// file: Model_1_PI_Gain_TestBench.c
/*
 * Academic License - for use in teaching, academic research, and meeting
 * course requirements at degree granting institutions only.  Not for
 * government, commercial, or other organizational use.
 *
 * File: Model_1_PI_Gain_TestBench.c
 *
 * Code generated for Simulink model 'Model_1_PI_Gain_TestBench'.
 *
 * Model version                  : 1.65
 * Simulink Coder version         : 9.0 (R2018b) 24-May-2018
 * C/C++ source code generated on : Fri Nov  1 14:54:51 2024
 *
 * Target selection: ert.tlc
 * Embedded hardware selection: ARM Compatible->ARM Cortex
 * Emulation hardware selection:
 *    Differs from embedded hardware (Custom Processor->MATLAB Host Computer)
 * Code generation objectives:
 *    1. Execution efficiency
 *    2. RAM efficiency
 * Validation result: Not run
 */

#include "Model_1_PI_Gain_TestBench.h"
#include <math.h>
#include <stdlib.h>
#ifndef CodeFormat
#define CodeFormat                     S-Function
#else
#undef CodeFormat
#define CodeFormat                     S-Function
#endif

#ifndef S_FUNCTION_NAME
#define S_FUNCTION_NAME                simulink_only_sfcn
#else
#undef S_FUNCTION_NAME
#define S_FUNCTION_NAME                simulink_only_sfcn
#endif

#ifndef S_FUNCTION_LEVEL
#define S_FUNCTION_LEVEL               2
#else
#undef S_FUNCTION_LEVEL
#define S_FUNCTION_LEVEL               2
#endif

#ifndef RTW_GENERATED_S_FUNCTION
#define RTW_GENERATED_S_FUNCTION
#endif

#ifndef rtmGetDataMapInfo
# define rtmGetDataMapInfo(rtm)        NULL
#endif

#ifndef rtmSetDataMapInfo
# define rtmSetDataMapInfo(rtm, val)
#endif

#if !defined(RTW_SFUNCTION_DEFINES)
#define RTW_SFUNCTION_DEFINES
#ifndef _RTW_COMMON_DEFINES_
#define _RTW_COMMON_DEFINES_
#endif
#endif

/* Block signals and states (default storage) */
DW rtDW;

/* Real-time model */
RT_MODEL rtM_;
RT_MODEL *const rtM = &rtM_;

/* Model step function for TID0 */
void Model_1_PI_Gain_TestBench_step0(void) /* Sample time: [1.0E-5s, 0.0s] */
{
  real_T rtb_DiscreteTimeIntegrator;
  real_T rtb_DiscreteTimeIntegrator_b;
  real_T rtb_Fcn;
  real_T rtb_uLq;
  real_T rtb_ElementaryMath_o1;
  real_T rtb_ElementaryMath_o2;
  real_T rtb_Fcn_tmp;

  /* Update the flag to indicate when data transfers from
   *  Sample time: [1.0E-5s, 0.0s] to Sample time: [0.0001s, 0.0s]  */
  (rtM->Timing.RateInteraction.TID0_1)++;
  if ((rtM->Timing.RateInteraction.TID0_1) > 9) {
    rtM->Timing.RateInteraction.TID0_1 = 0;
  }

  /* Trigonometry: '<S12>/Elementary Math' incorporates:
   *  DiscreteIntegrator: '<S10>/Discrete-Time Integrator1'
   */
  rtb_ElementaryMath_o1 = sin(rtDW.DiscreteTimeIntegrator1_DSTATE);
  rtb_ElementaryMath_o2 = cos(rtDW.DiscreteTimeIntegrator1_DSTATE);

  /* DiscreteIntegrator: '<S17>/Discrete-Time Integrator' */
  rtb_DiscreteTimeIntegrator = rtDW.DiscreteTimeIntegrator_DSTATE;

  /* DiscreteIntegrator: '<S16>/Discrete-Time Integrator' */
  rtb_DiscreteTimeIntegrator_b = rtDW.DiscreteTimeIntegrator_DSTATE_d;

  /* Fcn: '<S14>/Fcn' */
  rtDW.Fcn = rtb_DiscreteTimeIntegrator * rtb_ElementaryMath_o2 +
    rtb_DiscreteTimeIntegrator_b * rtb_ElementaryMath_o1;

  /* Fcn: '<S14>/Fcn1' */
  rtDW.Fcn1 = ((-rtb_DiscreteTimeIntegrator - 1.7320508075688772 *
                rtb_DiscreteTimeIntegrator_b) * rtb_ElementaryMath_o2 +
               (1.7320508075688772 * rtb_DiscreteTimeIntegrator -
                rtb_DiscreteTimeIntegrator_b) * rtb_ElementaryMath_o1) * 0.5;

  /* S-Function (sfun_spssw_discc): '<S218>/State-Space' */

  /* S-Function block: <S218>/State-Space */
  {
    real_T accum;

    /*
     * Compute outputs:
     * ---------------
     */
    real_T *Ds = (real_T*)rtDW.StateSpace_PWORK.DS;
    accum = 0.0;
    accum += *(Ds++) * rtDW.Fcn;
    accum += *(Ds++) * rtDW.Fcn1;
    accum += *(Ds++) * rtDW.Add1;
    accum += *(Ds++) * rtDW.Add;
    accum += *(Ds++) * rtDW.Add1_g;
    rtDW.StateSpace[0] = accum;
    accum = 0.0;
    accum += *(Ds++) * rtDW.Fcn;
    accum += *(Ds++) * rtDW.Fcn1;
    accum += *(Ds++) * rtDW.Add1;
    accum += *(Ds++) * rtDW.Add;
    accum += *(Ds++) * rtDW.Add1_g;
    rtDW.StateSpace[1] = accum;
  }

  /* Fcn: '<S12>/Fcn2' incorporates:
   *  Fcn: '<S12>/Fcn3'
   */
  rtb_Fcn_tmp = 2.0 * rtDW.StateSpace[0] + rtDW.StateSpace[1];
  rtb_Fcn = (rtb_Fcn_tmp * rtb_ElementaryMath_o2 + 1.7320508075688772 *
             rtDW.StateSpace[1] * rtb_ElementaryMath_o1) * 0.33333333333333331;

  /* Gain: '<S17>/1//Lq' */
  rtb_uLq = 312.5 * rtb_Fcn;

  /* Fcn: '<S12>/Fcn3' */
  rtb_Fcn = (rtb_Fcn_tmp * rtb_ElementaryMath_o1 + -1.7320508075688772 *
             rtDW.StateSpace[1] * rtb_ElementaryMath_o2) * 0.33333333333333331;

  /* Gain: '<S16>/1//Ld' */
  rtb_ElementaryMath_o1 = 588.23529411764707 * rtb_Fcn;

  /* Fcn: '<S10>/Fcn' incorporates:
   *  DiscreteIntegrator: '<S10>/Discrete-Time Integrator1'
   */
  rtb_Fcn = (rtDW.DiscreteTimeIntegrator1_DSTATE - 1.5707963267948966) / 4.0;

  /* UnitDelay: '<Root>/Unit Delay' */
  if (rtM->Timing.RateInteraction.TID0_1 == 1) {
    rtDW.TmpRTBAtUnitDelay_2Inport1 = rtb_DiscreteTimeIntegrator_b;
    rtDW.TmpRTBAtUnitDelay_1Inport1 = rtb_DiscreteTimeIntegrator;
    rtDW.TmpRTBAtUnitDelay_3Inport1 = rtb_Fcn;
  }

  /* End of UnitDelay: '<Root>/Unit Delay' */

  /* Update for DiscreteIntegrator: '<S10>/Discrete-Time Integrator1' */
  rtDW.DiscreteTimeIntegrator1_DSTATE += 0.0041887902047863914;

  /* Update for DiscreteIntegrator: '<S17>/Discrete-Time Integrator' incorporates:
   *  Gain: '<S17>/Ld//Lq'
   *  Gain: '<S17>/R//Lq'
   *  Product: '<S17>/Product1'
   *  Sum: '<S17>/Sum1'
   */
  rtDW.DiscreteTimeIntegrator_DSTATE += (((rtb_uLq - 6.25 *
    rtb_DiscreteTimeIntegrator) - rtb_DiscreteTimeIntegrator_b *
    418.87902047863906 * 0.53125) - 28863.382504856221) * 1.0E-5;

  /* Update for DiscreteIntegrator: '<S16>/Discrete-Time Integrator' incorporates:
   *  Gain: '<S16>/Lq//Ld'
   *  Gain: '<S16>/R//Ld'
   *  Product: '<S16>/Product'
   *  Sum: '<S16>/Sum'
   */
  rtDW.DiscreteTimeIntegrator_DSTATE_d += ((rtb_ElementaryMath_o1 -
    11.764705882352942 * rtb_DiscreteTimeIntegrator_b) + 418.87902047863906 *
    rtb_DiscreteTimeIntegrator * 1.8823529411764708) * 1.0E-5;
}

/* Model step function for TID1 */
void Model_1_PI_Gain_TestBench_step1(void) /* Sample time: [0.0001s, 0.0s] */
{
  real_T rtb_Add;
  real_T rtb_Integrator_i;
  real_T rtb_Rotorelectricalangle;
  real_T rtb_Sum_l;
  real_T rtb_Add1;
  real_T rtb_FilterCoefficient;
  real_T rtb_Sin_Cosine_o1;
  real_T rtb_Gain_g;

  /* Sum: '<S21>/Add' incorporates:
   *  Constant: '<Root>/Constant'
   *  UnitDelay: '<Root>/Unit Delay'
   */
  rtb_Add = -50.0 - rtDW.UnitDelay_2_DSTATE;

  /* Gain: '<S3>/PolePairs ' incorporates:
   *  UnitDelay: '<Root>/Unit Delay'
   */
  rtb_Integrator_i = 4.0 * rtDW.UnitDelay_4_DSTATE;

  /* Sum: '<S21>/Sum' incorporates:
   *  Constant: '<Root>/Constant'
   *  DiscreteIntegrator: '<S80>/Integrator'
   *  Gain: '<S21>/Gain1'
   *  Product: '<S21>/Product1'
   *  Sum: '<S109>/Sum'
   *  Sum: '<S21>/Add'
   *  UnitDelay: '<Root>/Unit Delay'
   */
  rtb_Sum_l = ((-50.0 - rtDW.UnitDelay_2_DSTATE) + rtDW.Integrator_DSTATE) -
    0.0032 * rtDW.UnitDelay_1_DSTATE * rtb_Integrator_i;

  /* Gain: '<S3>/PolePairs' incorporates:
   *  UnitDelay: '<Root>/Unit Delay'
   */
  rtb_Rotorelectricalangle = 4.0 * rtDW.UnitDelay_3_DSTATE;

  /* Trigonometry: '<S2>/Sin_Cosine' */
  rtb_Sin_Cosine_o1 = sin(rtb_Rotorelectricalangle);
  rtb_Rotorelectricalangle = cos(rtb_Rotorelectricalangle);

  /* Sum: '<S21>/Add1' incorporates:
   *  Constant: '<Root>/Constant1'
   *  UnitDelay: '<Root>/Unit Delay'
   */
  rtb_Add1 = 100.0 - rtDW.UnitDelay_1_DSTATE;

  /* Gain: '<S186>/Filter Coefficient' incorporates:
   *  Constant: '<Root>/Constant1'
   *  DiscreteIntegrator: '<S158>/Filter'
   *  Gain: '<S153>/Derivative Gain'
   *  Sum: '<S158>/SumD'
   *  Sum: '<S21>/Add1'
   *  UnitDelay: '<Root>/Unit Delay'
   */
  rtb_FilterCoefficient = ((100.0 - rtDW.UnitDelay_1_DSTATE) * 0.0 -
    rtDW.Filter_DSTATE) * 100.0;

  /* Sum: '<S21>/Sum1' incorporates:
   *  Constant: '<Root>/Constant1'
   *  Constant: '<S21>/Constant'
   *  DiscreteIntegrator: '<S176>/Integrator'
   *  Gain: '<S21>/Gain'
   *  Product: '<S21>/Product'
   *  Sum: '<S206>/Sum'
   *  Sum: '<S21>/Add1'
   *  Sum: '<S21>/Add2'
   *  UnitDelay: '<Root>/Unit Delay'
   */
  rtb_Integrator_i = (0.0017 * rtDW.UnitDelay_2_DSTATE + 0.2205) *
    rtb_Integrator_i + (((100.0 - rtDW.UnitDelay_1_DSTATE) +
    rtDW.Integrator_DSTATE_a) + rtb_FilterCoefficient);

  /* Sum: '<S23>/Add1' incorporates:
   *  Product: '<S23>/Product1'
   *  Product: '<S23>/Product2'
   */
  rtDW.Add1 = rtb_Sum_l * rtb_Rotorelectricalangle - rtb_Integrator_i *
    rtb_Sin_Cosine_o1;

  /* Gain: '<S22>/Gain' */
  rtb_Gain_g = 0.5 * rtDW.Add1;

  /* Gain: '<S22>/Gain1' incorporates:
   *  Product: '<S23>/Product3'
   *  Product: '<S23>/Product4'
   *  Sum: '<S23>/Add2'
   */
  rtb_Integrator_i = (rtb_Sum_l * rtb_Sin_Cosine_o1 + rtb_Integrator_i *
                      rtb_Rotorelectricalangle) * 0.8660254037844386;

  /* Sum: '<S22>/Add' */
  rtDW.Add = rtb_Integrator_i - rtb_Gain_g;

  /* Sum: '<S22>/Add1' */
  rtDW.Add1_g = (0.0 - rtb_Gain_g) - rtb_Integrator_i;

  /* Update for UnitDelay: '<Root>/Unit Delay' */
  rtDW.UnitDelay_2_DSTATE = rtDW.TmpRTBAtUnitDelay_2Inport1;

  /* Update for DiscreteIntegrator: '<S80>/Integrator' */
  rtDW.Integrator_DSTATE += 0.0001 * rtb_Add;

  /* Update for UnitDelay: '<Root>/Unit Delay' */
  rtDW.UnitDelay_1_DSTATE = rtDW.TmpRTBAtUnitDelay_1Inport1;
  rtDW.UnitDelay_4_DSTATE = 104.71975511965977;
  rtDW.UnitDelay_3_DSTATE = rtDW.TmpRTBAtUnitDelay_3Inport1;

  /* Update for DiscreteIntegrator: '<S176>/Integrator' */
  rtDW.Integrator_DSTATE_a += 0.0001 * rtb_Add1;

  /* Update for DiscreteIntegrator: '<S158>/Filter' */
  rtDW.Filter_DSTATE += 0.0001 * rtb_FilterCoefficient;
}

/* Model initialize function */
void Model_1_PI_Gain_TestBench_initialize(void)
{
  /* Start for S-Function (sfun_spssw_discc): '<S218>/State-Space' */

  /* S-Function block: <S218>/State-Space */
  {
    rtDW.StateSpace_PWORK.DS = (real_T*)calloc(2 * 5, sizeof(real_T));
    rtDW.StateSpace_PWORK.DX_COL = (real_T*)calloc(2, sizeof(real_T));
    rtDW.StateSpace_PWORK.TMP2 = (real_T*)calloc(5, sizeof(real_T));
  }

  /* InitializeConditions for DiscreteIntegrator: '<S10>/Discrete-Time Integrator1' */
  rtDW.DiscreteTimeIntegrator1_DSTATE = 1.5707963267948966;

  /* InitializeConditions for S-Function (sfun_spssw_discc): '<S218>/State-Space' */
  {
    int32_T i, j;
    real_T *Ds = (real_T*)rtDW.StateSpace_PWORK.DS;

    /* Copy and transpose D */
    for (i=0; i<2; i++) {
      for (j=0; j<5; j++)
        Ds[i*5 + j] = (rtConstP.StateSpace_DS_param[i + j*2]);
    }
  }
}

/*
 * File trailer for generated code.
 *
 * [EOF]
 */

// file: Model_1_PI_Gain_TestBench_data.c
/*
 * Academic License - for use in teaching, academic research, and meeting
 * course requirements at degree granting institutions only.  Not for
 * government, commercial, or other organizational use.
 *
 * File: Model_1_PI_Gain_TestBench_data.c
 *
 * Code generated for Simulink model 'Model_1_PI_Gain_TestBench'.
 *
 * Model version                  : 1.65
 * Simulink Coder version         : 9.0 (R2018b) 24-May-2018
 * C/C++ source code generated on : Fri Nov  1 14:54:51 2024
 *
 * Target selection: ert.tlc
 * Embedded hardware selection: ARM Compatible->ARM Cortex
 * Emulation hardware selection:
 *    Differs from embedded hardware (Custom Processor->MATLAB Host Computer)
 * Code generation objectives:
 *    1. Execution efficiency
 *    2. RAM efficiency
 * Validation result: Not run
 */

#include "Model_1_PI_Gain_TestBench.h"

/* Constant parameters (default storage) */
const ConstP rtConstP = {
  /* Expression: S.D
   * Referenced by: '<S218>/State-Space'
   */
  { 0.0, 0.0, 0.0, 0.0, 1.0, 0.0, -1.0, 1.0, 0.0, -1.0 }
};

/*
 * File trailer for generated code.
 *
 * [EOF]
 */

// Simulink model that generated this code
simulink model "Model_1_PI_Gain_TestBench"  (R2018b)
settings: Solver=FixedStepDiscrete  StartTime=0.0  StopTime=0.3  MaxStep=1e-4  RelTol=1e-3
values from neighbouring files (symbols this model uses):
  Gain_I = 1    [Model_1_Initialization.m]
  Gain_P = 1    [Model_1_Initialization.m]
  Id_reference = -50    [Model_1_Initialization.m]
  Iq_reference = 100    [Model_1_Initialization.m]
  Lambda_m = 0.2205    [Model_1_Initialization.m]
  Ld = 1.7e-3    (= 0.0017)    [Model_1_Initialization.m]
  Lq = 3.2e-3    (= 0.0032)    [Model_1_Initialization.m]
  Polepairs = 4    [Model_1_Initialization.m]
  Rs = 0.02    [Model_1_Initialization.m]
libraries: powerlib x6, simulink x2

== system Model_1_PI_Gain_TestBench ==
  note: Copyright 2018 The MathWorks, Inc.
  note: - Current closed-loop control
      | - Try Simulink Design Optimization(Analysis -> Response Optimization) to automate tuning the PI controller .  Initial condition: speed = 1000 rpm. (kp, ki) = (1,1)
      | - After tuning the current loop, try the simulation without dynamic decoupling control.
  note: Controller
  note: Plant
  note: FOC Control of PMSM
  " " : Subsystem
  Bus_Selector2 : BusSelector  OutputSignals=Stator current is_q (A)
  Constant : Constant  Value=Id_reference
  Constant1 : Constant  Value=Iq_reference  VectorParams1D=off
  FOC_Current_Control : Subsystem
  Mux : Mux  Inputs=2
  Scope2 : Scope
  Subsystem : Subsystem
  Subsystem1 : Subsystem
  Unit Delay : UnitDelay  SampleTime=1e-4
  powergui : powerlib/powergui  SimulationMode=Continuous  SampleTime=1e-5  frequency=60  Iterations=50  frequencyindice=0  Pbase=100e6  ErrMax=1e-4  UnitsV=kV  UnitsW=MW  buscounter=0  FunctionMessages=off  echomessages=off  EnableUseOfTLC=off  CurrentSourceSwitches=off  DisableSnubberDevices=off  DisableRonSwitches=off  DisableVfSwitches=off  DisplayEquations=off  SolverType=Tustin/Backward Euler (TBE)  Interpol=off  ExternalGateDelay=off  methode=off  Ts=100  x0status=blocks  SPID=on  SwTol=0  HookPort=off  RestoreLinks=warning  ResistiveCurrentMeasurement=off  Frange=[0:2:500]  Ylog=off  Xlog=on  ShowGrid=off  save=off  variable=ZData  structure=0  ZoomFFT=on  StartTime=0.0  cycles=1  DisplayStyle=1  fundamental=60  FreqAxis=off  MaxFrequency=1000  frequencyindicesteady=1  RmsSteady=1  display=off
  Scope : Scope
  Scope1 : Scope
  wires:
  FOC_Current_Control/1(Phase_Voltage) -> Subsystem1/1(In1)
  " "/1(measurements) -> Unit Delay/1, Bus_Selector2/1
  Subsystem/3(Out2) -> FOC_Current_Control/3(iq_feedback)
  Subsystem/4(Out3) -> FOC_Current_Control/4(id_feedback)
  Subsystem1/1(Out1) -> " "/1(Vabc)
  Unit Delay/1 -> Subsystem/3(PMSM_Measurements)
  Subsystem/5(Out1) -> FOC_Current_Control/5(speed_we)
  Subsystem/6(Out4) -> FOC_Current_Control/6(theta)
  Mux/1 -> Scope2/1
  Bus_Selector2/1 -> Mux/2  "<Stator current is_q (A)>"
  Constant/1 -> Subsystem/2(id_ref)
  Constant1/1 -> Mux/1, Subsystem/1(iq_ref)  "Iq_reference"
  Subsystem/1(Out6) -> FOC_Current_Control/1(iq_reference)
  Subsystem/2(Out5) -> FOC_Current_Control/2(id_reference)

== system Model_1_PI_Gain_TestBench/  ==
  Vabc : Inport
  Bus Creator : BusCreator  Inputs=4
  Bus Selector : BusSelector  OutputSignals=Stator current is_a (A),Stator current is_b (A),Stator current is_c (A),Stator current is_q (A),Stator current is_d (A),Rotor angle thetam (rad),Rotor speed wm (rad/s)
  Mux : Mux  Inputs=3
  Permanent Magnet Synchronous Machine [0.002 0.01 3 0] : powerlib/Machines/Permanent Magnet Synchronous Machine  NbPhases=3  FluxDistribution=Sinusoidal  RotorType=Salient-pole  MechanicalLoad=Speed w  PresetModel=No  ShowDetailedParameters=on  MeasurementBus=off  Resistance=Rs  Inductance=8.5e-3  dqInductances=[Ld,Lq]  La=0.000395  MachineConstant=Flux linkage established by magnets (V.s)  Flux=Lambda_m  VoltageCst=159.9771  TorqueCst=1.323  Flat=120  Mechanical=[0.0027 0.001 4 0]  PolePairs=Polepairs  InitialConditions=[0,0, 0,0]  InitialConditions5ph=[0 0 0 0 0 0]  TsPowergui=0  TsBlock=-1  RefAngle=Aligned with phase A axis (original Park)
  Terminator : Terminator
  ideal_voltage_so : Subsystem  VariantControl=variantPwm == enumPwm.behavior
  rpm : Constant  Value=1000
  "rpm -> rad/s" : Gain  Gain=2*pi/60
  measurements : Outport
  wires:
  Vabc/1 -> ideal_voltage_so/1(vabc)
  rpm/1 -> "rpm -> rad/s"/1
  Bus Selector/4 -> Bus Creator/1  "<Stator current is_q (A)>"
  Bus Selector/5 -> Bus Creator/2  "<Stator current is_d (A)>"
  Bus Selector/6 -> Bus Creator/3  "<Rotor angle thetam (rad)>"
  Bus Creator/1 -> measurements/1
  Bus Selector/1 -> Mux/1  "<Stator current is_a (A)>"
  Bus Selector/2 -> Mux/2  "<Stator current is_b (A)>"
  Bus Selector/3 -> Mux/3  "<Stator current is_c (A)>"
  Mux/1 -> Terminator/1
  Permanent Magnet Synchronous Machine [0.002 0.01 3 0]/1 -> Bus Selector/1
  Bus Selector/7 -> Bus Creator/4  "<Rotor speed wm (rad/s)>"
  "rpm -> rad/s"/1 -> Permanent Magnet Synchronous Machine [0.002 0.01 3 0]/1
  connections:
  Permanent Magnet Synchronous Machine [0.002 0.01 3 0]/LConn1 -- ideal_voltage_so/RConn1
  Permanent Magnet Synchronous Machine [0.002 0.01 3 0]/LConn2 -- ideal_voltage_so/RConn2
  Permanent Magnet Synchronous Machine [0.002 0.01 3 0]/LConn3 -- ideal_voltage_so/RConn3

== system Model_1_PI_Gain_TestBench/FOC_Current_Control ==
  iq_reference : Inport  SampleTime=1e-4
  id_reference : Inport  Port=2  SampleTime=1e-4
  iq_feedback : Inport  Port=3  SampleTime=1e-4
  id_feedback : Inport  Port=4  SampleTime=1e-4
  speed_we : Inport  Port=5  SampleTime=1e-4
  theta : Inport  Port=6  SampleTime=1e-4
  Current Controller : Subsystem
  Inverse Clarke Transform : Subsystem
  Inverse Park Transform : Subsystem
  Sin_Cosine : Trigonometry  Operator=sincos
  Phase_Voltage : Outport  SampleTime=1e-4
  wires:
  Inverse Clarke Transform/1(ABC) -> Phase_Voltage/1
  Sin_Cosine/2 -> Inverse Park Transform/4(Cos_Coefficient)
  Sin_Cosine/1 -> Inverse Park Transform/3(Sin_Coefficient)
  theta/1 -> Sin_Cosine/1
  Current Controller/2(vq_reference) -> Inverse Park Transform/2(Q)
  Current Controller/1(vd_reference) -> Inverse Park Transform/1(D)
  Inverse Park Transform/1(Alpha) -> Inverse Clarke Transform/1(Alpha)
  Inverse Park Transform/2(Beta) -> Inverse Clarke Transform/2(Beta)
  id_feedback/1 -> Current Controller/3(id_feedback)
  iq_feedback/1 -> Current Controller/4(iq_feedback)
  speed_we/1 -> Current Controller/5(spd_we)
  iq_reference/1 -> Current Controller/1(iq_reference)
  id_reference/1 -> Current Controller/2(id_reference)

== system Model_1_PI_Gain_TestBench/Subsystem ==
  note: Continuous To Discrete
  iq_ref : Inport
  id_ref : Inport  Port=2
  PMSM_Measurements : Inport  Port=3
  Bus_Selector2 : BusSelector  OutputSignals=Stator current is_q (A),Stator current is_d (A),Rotor speed wm (rad/s),Rotor angle thetam (rad)
  PolePairs : Gain  Gain=Polepairs
  "PolePairs " : Gain  Gain=Polepairs
  Rate_Transition{1..6} (6 alike) : RateTransition  Integrity=off  Deterministic=off
  Out6 : Outport
  Out5 : Outport  Port=2
  Out2 : Outport  Port=3
  Out3 : Outport  Port=4
  Out1 : Outport  Port=5
  Out4 : Outport  Port=6
  wires:
  Rate_Transition4/1 -> Out4/1
  Bus_Selector2/2 -> Rate_Transition3/1  "<Stator current is_d (A)>"
  id_ref/1 -> Rate_Transition5/1
  iq_ref/1 -> Rate_Transition6/1
  Bus_Selector2/1 -> Rate_Transition2/1  "<Stator current is_q (A)>"
  Bus_Selector2/4 -> PolePairs/1  "<Rotor angle thetam (rad)>"
  PMSM_Measurements/1 -> Bus_Selector2/1
  PolePairs/1 -> Rate_Transition4/1  "Rotor electrical angle"
  Rate_Transition5/1 -> Out5/1
  Rate_Transition6/1 -> Out6/1
  Rate_Transition2/1 -> Out2/1
  Rate_Transition3/1 -> Out3/1
  Rate_Transition1/1 -> Out1/1
  Bus_Selector2/3 -> "PolePairs "/1  "<Rotor speed wm (rad/s)>"
  "PolePairs "/1 -> Rate_Transition1/1  "Rotor electrical angular speed"

== system Model_1_PI_Gain_TestBench/Subsystem1 ==
  In1 : Inport
  Rate_Transition1 : RateTransition  Integrity=off
  Out1 : Outport
  wires:
  In1/1 -> Rate_Transition1/1
  Rate_Transition1/1 -> Out1/1

== system Model_1_PI_Gain_TestBench/ /ideal_voltage_so ==
  note: PWM Peripheral And Inverter
  vabc : Inport
  Controlled_Voltage_Source1 : powerlib/Electrical Sources/Controlled Voltage Source  Initialize=off  Source_Type=DC  Amplitude=12  Phase=0  Frequency=0  Measurements=None
  Controlled_Voltage_Source2 : powerlib/Electrical Sources/Controlled Voltage Source  Initialize=off  Source_Type=DC  Amplitude=12  Phase=0  Frequency=0  Measurements=None
  Controlled_Voltage_Source3 : powerlib/Electrical Sources/Controlled Voltage Source  Initialize=off  Source_Type=DC  Amplitude=12  Phase=0  Frequency=0  Measurements=None
  Ground2 : powerlib/Elements/Ground  LConnTagsString=a
  Selector3 : Selector  InputPortWidth=3  IndexOptions=Index vector (dialog)  Indices=[1]  OutputSizes=1
  Selector4 : Selector  InputPortWidth=3  IndexOptions=Index vector (dialog)  Indices=2  OutputSizes=1
  Selector5 : Selector  InputPortWidth=3  IndexOptions=Index vector (dialog)  Indices=3  OutputSizes=1
  A : PMIOPort  Tag=PMCPort  Side=Right
  B : PMIOPort  Tag=PMCPort  Port=2  Side=Right
  C : PMIOPort  Tag=PMCPort  Port=3  Side=Right
  wires:
  vabc/1 -> Selector4/1, Selector5/1, Selector3/1
  Selector5/1 -> Controlled_Voltage_Source3/1
  Selector4/1 -> Controlled_Voltage_Source2/1
  Selector3/1 -> Controlled_Voltage_Source1/1
  connections:
  C/RConn1 -- Controlled_Voltage_Source3/RConn1
  B/RConn1 -- Controlled_Voltage_Source2/RConn1
  A/RConn1 -- Controlled_Voltage_Source1/RConn1
  Controlled_Voltage_Source3/LConn1 -- Controlled_Voltage_Source1/LConn1 -- Controlled_Voltage_Source2/LConn1 -- Ground2/LConn1

== system Model_1_PI_Gain_TestBench/FOC_Current_Control/Current Controller ==
  note: Dynamic Decoupling Control
  iq_reference : Inport  SampleTime=1e-4
  id_reference : Inport  Port=2  SampleTime=1e-4
  id_feedback : Inport  Port=3  SampleTime=1e-4
  iq_feedback : Inport  Port=4  SampleTime=1e-4
  spd_we : Inport  Port=5  SampleTime=1e-4
  Add : Sum  Inputs=+-
  Add1 : Sum  Inputs=+-
  Add2 : Sum
  Constant : Constant  Value=Lambda_m  SampleTime=1e-4
  Gain : Gain  Gain=Ld
  Gain1 : Gain  Gain=Lq
  PID Controller : simulink/Continuous/PID Controller  Controller=PI  Form=Parallel  TimeDomain=Discrete-time  SampleTime=-1  IntegratorMethod=Forward Euler  FilterMethod=Forward Euler  ControllerParametersSource=internal  P=Gain_P  I=Gain_I  D=0  UseFilter=on  N=100  TunerSelectOption=Transfer Function Based (PID Tuner App)  InitialConditionSource=internal  InitialConditionForIntegrator=0  InitialConditionForFilter=0  DifferentiatorICPrevScaledInput=0  ExternalReset=none  TrackingMode=off  Kt=1  LimitOutput=off  UpperSaturationLimit=inf  LowerSaturationLimit=-inf  LinearizeAsGain=on  AntiWindupMode=none  Kb=1  POutMin=[]  POutMax=[]  IOutMin=[]  IOutMax=[]  DOutMin=[]  DOutMax=[]  NOutMin=[]  NOutMax=[]  SumOutMin=[]  SumOutMax=[]  SaturationOutMin=[]  SaturationOutMax=[]  PParamMin=[]  PParamMax=[]  IParamMin=[]  IParamMax=[]  DParamMin=[]  DParamMax=[]  NParamMin=[]  NParamMax=[]  KbParamMin=[]  KbParamMax=[]  KtParamMin=[]  KtParamMax=[]  KbOutMin=[]  KbOutMax=[]  KtOutMin=[]  KtOutMax=[]  IntegratorOutMin=[]  IntegratorOutMax=[]  FilterOutMin=[]  FilterOutMax=[]  SumI1OutMin=[]  SumI1OutMax=[]  SumI2OutMin=[]  SumI2OutMax=[]  SumI3OutMin=[]  SumI3OutMax=[]  SumI4OutMin=[]  SumI4OutMax=[]  SumDOutMin=[]  SumDOutMax=[]  DifferentiatorOutMin=[]  DifferentiatorOutMax=[]  FilterDiffOutCoefMin=[]  FilterDiffOutCoefMax=[]  ReciprocalOutMin=[]  ReciprocalOutMax=[]  SumDenOutMin=[]  SumDenOutMax=[]  SumNumOutMin=[]  SumNumOutMax=[]  DivideOutMin=[]  DivideOutMax=[]  IntegratorContinuousStateAttributes=''  IntegratorStateMustResolveToSignalObject=off  IntegratorRTWStateStorageClass=Auto  FilterContinuousStateAttributes=''  FilterStateMustResolveToSignalObject=off  FilterRTWStateStorageClass=Auto  ParallelPVariant=InternalParameters  IdealPVariant=Disabled  IVariant=InternalParameters  DVariant=Disabled  IntegratorVariant=Discrete  SatVariant=Disabled  AWVariant=Passthrough  PCopyVariant=Disabled  TRVariant=Disabled  FdbkBlocksVariant=Forward  IdealPFdbkVariant=Disabled  SatFdbkVariant=Disabled  DerivativeFilterVariant=Disabled  NVariant=Disabled  NCopyVariant=Disabled_SignalSpec  FilterICVariant=Disabled  IntegratorICVariant=InternalICs  ExternalResetVariant=Disabled  TRSumVariant=Passthrough  SumFdbkVariant=Disabled  SumVariant=Sum_PI
  PID Controller1 : simulink/Continuous/PID Controller  Controller=PID  Form=Parallel  TimeDomain=Discrete-time  SampleTime=-1  IntegratorMethod=Forward Euler  FilterMethod=Forward Euler  ControllerParametersSource=internal  P=Gain_P  I=Gain_I  D=0  UseFilter=on  N=100  TunerSelectOption=Transfer Function Based (PID Tuner App)  InitialConditionSource=internal  InitialConditionForIntegrator=0  InitialConditionForFilter=0  DifferentiatorICPrevScaledInput=0  ExternalReset=none  TrackingMode=off  Kt=1  LimitOutput=off  UpperSaturationLimit=inf  LowerSaturationLimit=-inf  LinearizeAsGain=on  AntiWindupMode=none  Kb=1  POutMin=[]  POutMax=[]  IOutMin=[]  IOutMax=[]  DOutMin=[]  DOutMax=[]  NOutMin=[]  NOutMax=[]  SumOutMin=[]  SumOutMax=[]  SaturationOutMin=[]  SaturationOutMax=[]  PParamMin=[]  PParamMax=[]  IParamMin=[]  IParamMax=[]  DParamMin=[]  DParamMax=[]  NParamMin=[]  NParamMax=[]  KbParamMin=[]  KbParamMax=[]  KtParamMin=[]  KtParamMax=[]  KbOutMin=[]  KbOutMax=[]  KtOutMin=[]  KtOutMax=[]  IntegratorOutMin=[]  IntegratorOutMax=[]  FilterOutMin=[]  FilterOutMax=[]  SumI1OutMin=[]  SumI1OutMax=[]  SumI2OutMin=[]  SumI2OutMax=[]  SumI3OutMin=[]  SumI3OutMax=[]  SumI4OutMin=[]  SumI4OutMax=[]  SumDOutMin=[]  SumDOutMax=[]  DifferentiatorOutMin=[]  DifferentiatorOutMax=[]  FilterDiffOutCoefMin=[]  FilterDiffOutCoefMax=[]  ReciprocalOutMin=[]  ReciprocalOutMax=[]  SumDenOutMin=[]  SumDenOutMax=[]  SumNumOutMin=[]  SumNumOutMax=[]  DivideOutMin=[]  DivideOutMax=[]  IntegratorContinuousStateAttributes=''  IntegratorStateMustResolveToSignalObject=off  IntegratorRTWStateStorageClass=Auto  FilterContinuousStateAttributes=''  FilterStateMustResolveToSignalObject=off  FilterRTWStateStorageClass=Auto  ParallelPVariant=InternalParameters  IdealPVariant=Disabled  IVariant=InternalParameters  DVariant=InternalParameters  IntegratorVariant=Discrete  SatVariant=Disabled  AWVariant=Passthrough  PCopyVariant=Disabled  TRVariant=Disabled  FdbkBlocksVariant=Forward  IdealPFdbkVariant=Disabled  SatFdbkVariant=Disabled  DerivativeFilterVariant=ForwardEulerFilter  NVariant=InternalParameters  NCopyVariant=Disabled  FilterICVariant=InternalICsFilter  IntegratorICVariant=InternalICs  ExternalResetVariant=Disabled  TRSumVariant=Passthrough  SumFdbkVariant=Disabled  SumVariant=Sum_PID
  Product : Product
  Product1 : Product
  Sum : Sum  Inputs=|+-
  Sum1 : Sum  Inputs=++|
  vd_reference : Outport  SampleTime=1e-4
  vq_reference : Outport  Port=2  SampleTime=1e-4
  wires:
  Sum/1 -> vd_reference/1
  PID Controller/1 -> Sum/1
  id_feedback/1 -> Gain/1, Add/2
  Add/1 -> PID Controller/1
  iq_feedback/1 -> Gain1/1, Add1/2
  id_reference/1 -> Add/1
  Add1/1 -> PID Controller1/1
  iq_reference/1 -> Add1/1
  Sum1/1 -> vq_reference/1
  PID Controller1/1 -> Sum1/2
  Gain/1 -> Add2/1
  Constant/1 -> Add2/2
  Add2/1 -> Product/2
  spd_we/1 -> Product1/2, Product/1
  Gain1/1 -> Product1/1
  Product1/1 -> Sum/2
  Product/1 -> Sum1/1

== system Model_1_PI_Gain_TestBench/FOC_Current_Control/Inverse Clarke Transform ==
  note: Inverse Clarke Transform
  note: Converts direct axis (alpha) component and the quadrature axis (beta) component to balanced three-phase quantities
      | The alpha and beta components are dependent on time and speed.
  Alpha : Inport
  Beta : Inport  Port=2
  Add : Sum  Inputs=-+  OutDataTypeStr=Inherit: Same as first input
  Add1 : Sum  Inputs=--  OutDataTypeStr=Inherit: Same as first input
  Gain : Gain  Gain=1/2
  Gain1 : Gain  Gain=sqrt(3)/2
  Mux : Mux  Inputs=3
  ABC : Outport
  wires:
  Beta/1 -> Gain1/1
  Mux/1 -> ABC/1
  Alpha/1 -> Mux/1, Gain/1
  Add1/1 -> Mux/3
  Gain1/1 -> Add1/2, Add/2
  Gain/1 -> Add1/1, Add/1
  Add/1 -> Mux/2

== system Model_1_PI_Gain_TestBench/FOC_Current_Control/Inverse Park Transform ==
  note: Converts orthogonal rotating reference frame (dq) to two-phase orthogonal stationary reference frame (alpha, beta)
  note: Inverse Park Transform
  D : Inport
  Q : Inport  Port=2
  Sin_Coefficient : Inport  Port=3
  Cos_Coefficient : Inport  Port=4
  Add1 : Sum  Inputs=+-  OutDataTypeStr=Inherit: Same as first input
  Add2 : Sum  OutDataTypeStr=Inherit: Same as first input
  Cos_Coefficient_1 : InportShadow  Port=4
  Product{1..4} (4 alike) : Product  RndMeth=Simplest
  Sin_Coefficient_1 : InportShadow  Port=3
  Alpha : Outport
  Beta : Outport  Port=2
  wires:
  Sin_Coefficient_1/1 -> Product3/2
  Product2/1 -> Add1/2
  Cos_Coefficient_1/1 -> Product4/2
  Add2/1 -> Beta/1
  Product3/1 -> Add2/1
  Add1/1 -> Alpha/1
  Product1/1 -> Add1/1
  Product4/1 -> Add2/2
  Sin_Coefficient/1 -> Product2/2
  D/1 -> Product3/1, Product1/1
  Q/1 -> Product2/1, Product4/1
  Cos_Coefficient/1 -> Product1/2
